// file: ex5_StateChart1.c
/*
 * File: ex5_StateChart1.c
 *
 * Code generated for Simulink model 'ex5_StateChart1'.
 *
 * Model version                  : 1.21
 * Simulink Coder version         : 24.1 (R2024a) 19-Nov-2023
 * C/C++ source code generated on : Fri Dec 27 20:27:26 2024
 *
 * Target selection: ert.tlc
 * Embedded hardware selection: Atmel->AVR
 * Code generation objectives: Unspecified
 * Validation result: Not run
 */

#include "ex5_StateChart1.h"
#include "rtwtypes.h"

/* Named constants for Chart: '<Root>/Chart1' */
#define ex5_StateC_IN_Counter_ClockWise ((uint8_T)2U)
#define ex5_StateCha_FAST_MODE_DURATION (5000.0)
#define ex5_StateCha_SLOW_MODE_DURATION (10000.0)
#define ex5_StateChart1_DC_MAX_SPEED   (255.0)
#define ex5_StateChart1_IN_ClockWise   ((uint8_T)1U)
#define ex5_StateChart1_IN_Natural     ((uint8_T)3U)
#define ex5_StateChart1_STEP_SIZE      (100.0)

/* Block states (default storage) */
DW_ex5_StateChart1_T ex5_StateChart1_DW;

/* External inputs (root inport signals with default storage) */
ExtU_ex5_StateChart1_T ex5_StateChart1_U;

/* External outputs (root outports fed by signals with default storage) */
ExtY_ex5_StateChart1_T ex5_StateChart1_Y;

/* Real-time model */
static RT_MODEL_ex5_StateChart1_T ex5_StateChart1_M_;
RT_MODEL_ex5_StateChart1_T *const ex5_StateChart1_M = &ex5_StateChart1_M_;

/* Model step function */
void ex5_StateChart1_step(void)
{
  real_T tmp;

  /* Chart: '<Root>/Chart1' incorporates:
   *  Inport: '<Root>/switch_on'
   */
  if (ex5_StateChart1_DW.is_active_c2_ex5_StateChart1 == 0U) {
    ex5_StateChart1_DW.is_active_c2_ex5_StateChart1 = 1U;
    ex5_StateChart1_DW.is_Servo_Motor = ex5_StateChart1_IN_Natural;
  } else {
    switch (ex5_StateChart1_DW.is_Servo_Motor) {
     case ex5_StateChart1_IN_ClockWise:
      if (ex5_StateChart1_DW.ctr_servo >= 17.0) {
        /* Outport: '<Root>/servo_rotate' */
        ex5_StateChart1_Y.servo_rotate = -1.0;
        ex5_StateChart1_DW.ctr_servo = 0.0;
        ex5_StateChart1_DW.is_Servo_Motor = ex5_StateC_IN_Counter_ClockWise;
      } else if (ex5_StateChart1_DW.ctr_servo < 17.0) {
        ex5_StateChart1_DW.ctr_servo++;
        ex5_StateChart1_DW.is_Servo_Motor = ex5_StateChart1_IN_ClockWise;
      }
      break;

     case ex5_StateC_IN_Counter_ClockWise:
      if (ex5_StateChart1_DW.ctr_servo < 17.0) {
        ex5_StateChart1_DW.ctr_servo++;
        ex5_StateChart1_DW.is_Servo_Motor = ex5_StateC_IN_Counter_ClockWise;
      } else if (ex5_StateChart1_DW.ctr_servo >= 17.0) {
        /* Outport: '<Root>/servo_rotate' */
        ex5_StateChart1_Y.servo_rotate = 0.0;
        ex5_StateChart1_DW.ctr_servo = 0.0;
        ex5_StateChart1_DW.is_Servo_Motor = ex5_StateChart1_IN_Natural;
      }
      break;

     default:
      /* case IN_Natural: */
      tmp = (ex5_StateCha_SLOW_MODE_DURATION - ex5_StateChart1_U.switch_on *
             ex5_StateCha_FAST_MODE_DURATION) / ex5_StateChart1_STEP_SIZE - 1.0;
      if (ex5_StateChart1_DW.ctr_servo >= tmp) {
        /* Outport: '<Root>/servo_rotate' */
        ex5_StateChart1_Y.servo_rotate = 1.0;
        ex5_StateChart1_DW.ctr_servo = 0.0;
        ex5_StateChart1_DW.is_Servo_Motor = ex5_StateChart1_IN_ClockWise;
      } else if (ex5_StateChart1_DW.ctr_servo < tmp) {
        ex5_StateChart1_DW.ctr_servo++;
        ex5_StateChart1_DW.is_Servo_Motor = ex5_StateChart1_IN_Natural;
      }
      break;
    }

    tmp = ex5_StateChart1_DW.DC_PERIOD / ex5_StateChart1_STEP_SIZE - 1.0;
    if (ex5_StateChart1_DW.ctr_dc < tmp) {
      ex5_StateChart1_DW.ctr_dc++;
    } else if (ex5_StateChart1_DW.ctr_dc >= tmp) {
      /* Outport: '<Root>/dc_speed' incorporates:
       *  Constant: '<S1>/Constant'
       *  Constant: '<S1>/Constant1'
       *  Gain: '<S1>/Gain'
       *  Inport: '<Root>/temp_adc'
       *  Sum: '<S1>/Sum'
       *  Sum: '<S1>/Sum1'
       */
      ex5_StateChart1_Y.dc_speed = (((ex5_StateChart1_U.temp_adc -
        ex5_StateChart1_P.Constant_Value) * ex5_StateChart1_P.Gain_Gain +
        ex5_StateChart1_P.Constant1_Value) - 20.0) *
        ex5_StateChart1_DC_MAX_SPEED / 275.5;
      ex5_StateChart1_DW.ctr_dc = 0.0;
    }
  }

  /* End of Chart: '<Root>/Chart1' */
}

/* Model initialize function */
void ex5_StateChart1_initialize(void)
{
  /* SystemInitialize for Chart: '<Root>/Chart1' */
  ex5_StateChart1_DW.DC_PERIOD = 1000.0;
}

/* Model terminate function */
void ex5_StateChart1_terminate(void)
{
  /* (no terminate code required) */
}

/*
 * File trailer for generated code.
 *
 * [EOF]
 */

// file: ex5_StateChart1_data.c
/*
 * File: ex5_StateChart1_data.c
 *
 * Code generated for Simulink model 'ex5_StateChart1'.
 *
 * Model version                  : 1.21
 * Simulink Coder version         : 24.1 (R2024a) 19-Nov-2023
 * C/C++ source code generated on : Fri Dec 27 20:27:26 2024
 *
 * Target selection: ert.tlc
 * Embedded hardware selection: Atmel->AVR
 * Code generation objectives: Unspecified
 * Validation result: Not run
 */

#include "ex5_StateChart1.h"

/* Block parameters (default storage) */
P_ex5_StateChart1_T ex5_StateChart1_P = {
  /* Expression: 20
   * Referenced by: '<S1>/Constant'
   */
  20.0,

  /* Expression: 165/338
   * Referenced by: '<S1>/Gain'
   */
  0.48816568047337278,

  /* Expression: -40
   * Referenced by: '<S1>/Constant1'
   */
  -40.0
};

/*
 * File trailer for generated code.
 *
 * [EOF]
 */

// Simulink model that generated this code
simulink model "ex5_StateChart1"  (R2024a)
settings: Solver=FixedStepDiscrete  StartTime=0.0  StopTime=20.0  FixedStep=0.1  RelTol=1e-3  EnableMultiTasking=on

== system ex5_StateChart1 ==
  temp_adc : Inport
  switch_on : Inport  Port=2
  CelsiusScaler Subsystem : Subsystem
  Chart1 : Stateflow chart  TreatAsAtomicUnit=on
  servo_rotate : Outport
  dc_speed : Outport  Port=2
  wires:
  temp_adc/1 -> CelsiusScaler Subsystem/1(tmp_adc)
  Chart1/1(servo_rotate) -> servo_rotate/1
  Chart1/2(dc_speed) -> dc_speed/1
  CelsiusScaler Subsystem/1(celsius) -> Chart1/2(celsius)
  switch_on/1 -> Chart1/1(switch_on)

== system ex5_StateChart1/CelsiusScaler Subsystem ==
  tmp_adc : Inport
  Constant : Constant  Value=20
  Constant1 : Constant  Value=-40
  Gain : Gain  Gain=165/338
  Sum : Sum  Inputs=|+-
  Sum1 : Sum  Inputs=|++
  celsius : Outport
  wires:
  Constant/1 -> Sum/2
  tmp_adc/1 -> Sum/1
  Constant1/1 -> Sum1/2
  Gain/1 -> Sum1/1
  Sum1/1 -> celsius/1
  Sum/1 -> Gain/1

== stateflow chart ex5_StateChart1/Chart1 ==
  state DC_Motor [parallel]
    settings: executionOrder=2
    state check
    check -> check [order 1] : [ctr_dc < (DC_PERIOD / STEP_SIZE) - 1]{ctr_dc = ctr_dc + 1}
    (default) -> check
    check -> check [order 2] : [ctr_dc >= (DC_PERIOD / STEP_SIZE) - 1]{dc_speed = (celsius - 20) * DC_MAX_SPEED / (DC_MAX_RPM / 60); ctr_dc = 0;}
  state Servo_Motor [parallel]
    settings: executionOrder=1
    state Natural
    state ClockWise
    state Counter_ClockWise
    (default) -> Natural
    Natural -> Natural [order 2] : [ctr_servo < ((SLOW_MODE_DURATION - (switch_on * (SLOW_MODE_DURATION - FAST_MODE_DURATION))) / STEP_SIZE) - 1]{ctr_servo = ctr_servo + 1}
    Counter_ClockWise -> Natural [order 2] : [ctr_servo >= (SERVO_MAX_ANGLE / SERVO_ANGLE_CHANGE) - 1]{servo_rotate = 0; ctr_servo = 0}
    Natural -> ClockWise [order 1] : [ctr_servo >= ((SLOW_MODE_DURATION - (switch_on * (SLOW_MODE_DURATION - FAST_MODE_DURATION))) / STEP_SIZE) - 1]{servo_rotate = 1; ctr_servo = 0}
    ClockWise -> ClockWise [order 2] : [ctr_servo < (SERVO_MAX_ANGLE / SERVO_ANGLE_CHANGE) - 1]{ctr_servo = ctr_servo + 1}
    ClockWise -> Counter_ClockWise [order 1] : [ctr_servo >= (SERVO_MAX_ANGLE / SERVO_ANGLE_CHANGE) - 1]{servo_rotate = -1; ctr_servo = 0}
    Counter_ClockWise -> Counter_ClockWise [order 1] : [ctr_servo < (SERVO_MAX_ANGLE / SERVO_ANGLE_CHANGE) - 1]{ctr_servo = ctr_servo + 1}
  data: SLOW_MODE_DURATION constant double =10000; servo_rotate output =0; FAST_MODE_DURATION constant double =5000; STEP_SIZE constant double =100; switch_on input; ctr_dc local =0; ctr_servo local =0; SERVO_MAX_ANGLE constant double =180; SERVO_ANGLE_CHANGE constant double =10; DC_PERIOD local =1000; dc_speed output =0; celsius input; DC_MAX_RPM constant double =16530; DC_MAX_SPEED constant double =255
